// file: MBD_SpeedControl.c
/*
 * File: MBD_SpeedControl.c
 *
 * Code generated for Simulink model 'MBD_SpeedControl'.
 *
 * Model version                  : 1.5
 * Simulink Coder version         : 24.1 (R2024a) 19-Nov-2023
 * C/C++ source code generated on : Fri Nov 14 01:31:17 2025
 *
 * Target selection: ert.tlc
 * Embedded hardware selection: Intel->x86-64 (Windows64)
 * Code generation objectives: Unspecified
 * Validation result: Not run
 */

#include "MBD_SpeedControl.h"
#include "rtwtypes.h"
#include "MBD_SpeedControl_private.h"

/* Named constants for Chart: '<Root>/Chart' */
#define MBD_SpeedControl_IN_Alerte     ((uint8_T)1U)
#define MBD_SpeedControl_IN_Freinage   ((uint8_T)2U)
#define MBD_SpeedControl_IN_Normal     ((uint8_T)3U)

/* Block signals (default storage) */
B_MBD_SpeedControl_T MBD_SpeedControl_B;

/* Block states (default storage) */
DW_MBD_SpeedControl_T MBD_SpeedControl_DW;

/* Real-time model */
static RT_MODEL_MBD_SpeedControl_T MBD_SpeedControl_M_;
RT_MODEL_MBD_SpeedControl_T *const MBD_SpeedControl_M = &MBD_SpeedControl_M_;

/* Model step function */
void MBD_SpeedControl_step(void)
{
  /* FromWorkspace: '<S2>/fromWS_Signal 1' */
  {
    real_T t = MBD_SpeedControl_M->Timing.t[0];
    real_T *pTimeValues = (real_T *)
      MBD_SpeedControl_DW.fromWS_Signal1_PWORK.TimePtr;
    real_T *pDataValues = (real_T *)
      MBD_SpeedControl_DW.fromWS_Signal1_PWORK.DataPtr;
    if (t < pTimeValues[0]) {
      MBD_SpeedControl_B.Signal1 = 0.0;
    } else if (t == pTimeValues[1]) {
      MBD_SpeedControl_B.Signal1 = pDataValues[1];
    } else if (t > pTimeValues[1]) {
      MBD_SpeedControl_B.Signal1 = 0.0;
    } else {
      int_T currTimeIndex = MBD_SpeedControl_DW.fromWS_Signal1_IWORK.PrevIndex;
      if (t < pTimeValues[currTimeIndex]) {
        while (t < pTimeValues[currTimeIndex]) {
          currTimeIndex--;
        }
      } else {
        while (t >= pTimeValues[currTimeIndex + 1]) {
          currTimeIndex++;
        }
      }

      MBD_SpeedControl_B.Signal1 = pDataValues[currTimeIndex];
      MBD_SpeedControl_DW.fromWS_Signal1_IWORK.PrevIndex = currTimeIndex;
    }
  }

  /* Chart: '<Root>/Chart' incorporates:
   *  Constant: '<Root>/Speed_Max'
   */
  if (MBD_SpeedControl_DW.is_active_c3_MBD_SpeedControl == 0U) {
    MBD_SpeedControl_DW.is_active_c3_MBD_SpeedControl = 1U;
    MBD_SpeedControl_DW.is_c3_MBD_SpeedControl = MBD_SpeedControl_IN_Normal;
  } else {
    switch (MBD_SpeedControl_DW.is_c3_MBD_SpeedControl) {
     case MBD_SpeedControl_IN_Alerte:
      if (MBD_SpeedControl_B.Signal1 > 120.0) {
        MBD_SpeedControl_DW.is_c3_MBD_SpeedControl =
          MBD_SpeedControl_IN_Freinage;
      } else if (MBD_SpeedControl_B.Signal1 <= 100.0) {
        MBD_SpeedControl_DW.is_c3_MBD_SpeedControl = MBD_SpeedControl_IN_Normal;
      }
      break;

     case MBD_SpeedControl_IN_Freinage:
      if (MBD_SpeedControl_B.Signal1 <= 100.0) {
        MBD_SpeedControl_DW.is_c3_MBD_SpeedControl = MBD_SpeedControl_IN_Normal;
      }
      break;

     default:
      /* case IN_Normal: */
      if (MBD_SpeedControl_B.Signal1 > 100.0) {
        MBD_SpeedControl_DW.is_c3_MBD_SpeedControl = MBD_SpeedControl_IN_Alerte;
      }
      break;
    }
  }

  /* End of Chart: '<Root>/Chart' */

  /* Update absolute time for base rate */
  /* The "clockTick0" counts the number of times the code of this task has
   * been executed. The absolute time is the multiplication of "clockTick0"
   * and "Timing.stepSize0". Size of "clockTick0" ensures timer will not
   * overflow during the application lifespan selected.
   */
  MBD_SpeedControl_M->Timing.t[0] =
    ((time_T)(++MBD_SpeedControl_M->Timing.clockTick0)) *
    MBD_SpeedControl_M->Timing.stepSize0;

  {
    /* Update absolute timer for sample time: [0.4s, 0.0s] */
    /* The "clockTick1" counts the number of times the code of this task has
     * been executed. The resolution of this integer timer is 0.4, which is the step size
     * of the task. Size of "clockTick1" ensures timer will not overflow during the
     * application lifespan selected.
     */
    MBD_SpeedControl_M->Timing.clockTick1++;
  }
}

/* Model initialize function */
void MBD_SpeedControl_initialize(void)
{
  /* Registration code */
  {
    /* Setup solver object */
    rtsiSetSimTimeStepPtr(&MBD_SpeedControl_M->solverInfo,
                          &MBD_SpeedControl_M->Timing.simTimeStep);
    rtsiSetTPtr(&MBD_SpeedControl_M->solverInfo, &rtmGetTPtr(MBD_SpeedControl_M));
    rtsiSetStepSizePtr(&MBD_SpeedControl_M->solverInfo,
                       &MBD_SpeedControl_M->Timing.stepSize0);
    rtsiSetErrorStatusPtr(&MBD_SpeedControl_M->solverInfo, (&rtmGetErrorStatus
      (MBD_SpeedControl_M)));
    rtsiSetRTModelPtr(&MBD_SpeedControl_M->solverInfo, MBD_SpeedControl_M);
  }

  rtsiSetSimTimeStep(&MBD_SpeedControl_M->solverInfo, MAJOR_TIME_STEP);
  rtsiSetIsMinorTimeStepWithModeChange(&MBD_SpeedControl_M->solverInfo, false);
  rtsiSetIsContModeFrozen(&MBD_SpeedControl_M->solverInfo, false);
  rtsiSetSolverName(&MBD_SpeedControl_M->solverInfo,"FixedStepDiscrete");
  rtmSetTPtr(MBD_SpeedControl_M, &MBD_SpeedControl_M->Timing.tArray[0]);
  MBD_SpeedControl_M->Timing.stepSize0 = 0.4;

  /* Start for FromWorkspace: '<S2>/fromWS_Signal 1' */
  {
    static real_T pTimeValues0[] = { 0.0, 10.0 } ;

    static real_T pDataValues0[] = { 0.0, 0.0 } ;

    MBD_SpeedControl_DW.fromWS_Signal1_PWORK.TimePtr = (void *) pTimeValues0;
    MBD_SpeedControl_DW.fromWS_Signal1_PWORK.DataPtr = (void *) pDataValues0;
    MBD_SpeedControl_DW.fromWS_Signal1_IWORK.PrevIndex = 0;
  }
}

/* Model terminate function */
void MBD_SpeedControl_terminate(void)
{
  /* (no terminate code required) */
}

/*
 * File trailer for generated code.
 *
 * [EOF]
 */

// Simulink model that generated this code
simulink model "MBD_SpeedControl"  (R2024a)
settings: Solver=FixedStepDiscrete  StartTime=0.0  StopTime=20.0  RelTol=1e-3
libraries: SignalEditorBlockLib x1

== system MBD_SpeedControl ==
  Chart : Stateflow chart  TreatAsAtomicUnit=on
  Display : Display
  Display1 : Display
  Scope : Scope
  Scope1 : Scope
  Speed : SignalEditorBlockLib/Signal Editor  FileName=C:\Users\Hakima Ayed\Desktop\Vitesse\vitesse simulé d'une voiture.mat  ActiveScenario=Scenario  ActiveSignal=Signal 1  IsBus=off  OutputBusObjectStr=Bus: BusObject  SampleTime=0  Interpolate=off  ZeroCross=off  OutputAfterFinalValue=Setting to zero  Unit=inherit  PreserveSignalName=on  ApplySigPropsToAllScenarios=on  ApplySigPropsToAllSignals=off
  Speed_Max : Constant  Value=100
  wires:
  Speed_Max/1 -> Chart/2(Speed_Max)
  Chart/1(OverSpeed_Alert) -> Display1/1
  Chart/2(Brake_Command) -> Scope/1
  Speed/1 -> Scope1/1, Display/1, Chart/1(Speed)

== stateflow chart MBD_SpeedControl/Chart ==
  state Alerte
    OverSpeed_Alert = true;
    Brake_Command = false;
  state Freinage
    OverSpeed_Alert = true;
    Brake_Command = true;
  state Normal
    OverSpeed_Alert = false;
    Brake_Command=false;
  Normal -> Alerte : [Speed > Speed_Max
      | ]
  Alerte -> Freinage [order 1] : [Speed > Speed_Max + 20
      | ]
  Alerte -> Normal [order 2] : [Speed <= Speed_Max
      | ]
  (default) -> Normal
  Freinage -> Normal : [Speed <= Speed_Max
      | ]
  data: Speed input size=1; Speed_Max input size=1; OverSpeed_Alert output boolean size=1; Brake_Command output boolean size=1
